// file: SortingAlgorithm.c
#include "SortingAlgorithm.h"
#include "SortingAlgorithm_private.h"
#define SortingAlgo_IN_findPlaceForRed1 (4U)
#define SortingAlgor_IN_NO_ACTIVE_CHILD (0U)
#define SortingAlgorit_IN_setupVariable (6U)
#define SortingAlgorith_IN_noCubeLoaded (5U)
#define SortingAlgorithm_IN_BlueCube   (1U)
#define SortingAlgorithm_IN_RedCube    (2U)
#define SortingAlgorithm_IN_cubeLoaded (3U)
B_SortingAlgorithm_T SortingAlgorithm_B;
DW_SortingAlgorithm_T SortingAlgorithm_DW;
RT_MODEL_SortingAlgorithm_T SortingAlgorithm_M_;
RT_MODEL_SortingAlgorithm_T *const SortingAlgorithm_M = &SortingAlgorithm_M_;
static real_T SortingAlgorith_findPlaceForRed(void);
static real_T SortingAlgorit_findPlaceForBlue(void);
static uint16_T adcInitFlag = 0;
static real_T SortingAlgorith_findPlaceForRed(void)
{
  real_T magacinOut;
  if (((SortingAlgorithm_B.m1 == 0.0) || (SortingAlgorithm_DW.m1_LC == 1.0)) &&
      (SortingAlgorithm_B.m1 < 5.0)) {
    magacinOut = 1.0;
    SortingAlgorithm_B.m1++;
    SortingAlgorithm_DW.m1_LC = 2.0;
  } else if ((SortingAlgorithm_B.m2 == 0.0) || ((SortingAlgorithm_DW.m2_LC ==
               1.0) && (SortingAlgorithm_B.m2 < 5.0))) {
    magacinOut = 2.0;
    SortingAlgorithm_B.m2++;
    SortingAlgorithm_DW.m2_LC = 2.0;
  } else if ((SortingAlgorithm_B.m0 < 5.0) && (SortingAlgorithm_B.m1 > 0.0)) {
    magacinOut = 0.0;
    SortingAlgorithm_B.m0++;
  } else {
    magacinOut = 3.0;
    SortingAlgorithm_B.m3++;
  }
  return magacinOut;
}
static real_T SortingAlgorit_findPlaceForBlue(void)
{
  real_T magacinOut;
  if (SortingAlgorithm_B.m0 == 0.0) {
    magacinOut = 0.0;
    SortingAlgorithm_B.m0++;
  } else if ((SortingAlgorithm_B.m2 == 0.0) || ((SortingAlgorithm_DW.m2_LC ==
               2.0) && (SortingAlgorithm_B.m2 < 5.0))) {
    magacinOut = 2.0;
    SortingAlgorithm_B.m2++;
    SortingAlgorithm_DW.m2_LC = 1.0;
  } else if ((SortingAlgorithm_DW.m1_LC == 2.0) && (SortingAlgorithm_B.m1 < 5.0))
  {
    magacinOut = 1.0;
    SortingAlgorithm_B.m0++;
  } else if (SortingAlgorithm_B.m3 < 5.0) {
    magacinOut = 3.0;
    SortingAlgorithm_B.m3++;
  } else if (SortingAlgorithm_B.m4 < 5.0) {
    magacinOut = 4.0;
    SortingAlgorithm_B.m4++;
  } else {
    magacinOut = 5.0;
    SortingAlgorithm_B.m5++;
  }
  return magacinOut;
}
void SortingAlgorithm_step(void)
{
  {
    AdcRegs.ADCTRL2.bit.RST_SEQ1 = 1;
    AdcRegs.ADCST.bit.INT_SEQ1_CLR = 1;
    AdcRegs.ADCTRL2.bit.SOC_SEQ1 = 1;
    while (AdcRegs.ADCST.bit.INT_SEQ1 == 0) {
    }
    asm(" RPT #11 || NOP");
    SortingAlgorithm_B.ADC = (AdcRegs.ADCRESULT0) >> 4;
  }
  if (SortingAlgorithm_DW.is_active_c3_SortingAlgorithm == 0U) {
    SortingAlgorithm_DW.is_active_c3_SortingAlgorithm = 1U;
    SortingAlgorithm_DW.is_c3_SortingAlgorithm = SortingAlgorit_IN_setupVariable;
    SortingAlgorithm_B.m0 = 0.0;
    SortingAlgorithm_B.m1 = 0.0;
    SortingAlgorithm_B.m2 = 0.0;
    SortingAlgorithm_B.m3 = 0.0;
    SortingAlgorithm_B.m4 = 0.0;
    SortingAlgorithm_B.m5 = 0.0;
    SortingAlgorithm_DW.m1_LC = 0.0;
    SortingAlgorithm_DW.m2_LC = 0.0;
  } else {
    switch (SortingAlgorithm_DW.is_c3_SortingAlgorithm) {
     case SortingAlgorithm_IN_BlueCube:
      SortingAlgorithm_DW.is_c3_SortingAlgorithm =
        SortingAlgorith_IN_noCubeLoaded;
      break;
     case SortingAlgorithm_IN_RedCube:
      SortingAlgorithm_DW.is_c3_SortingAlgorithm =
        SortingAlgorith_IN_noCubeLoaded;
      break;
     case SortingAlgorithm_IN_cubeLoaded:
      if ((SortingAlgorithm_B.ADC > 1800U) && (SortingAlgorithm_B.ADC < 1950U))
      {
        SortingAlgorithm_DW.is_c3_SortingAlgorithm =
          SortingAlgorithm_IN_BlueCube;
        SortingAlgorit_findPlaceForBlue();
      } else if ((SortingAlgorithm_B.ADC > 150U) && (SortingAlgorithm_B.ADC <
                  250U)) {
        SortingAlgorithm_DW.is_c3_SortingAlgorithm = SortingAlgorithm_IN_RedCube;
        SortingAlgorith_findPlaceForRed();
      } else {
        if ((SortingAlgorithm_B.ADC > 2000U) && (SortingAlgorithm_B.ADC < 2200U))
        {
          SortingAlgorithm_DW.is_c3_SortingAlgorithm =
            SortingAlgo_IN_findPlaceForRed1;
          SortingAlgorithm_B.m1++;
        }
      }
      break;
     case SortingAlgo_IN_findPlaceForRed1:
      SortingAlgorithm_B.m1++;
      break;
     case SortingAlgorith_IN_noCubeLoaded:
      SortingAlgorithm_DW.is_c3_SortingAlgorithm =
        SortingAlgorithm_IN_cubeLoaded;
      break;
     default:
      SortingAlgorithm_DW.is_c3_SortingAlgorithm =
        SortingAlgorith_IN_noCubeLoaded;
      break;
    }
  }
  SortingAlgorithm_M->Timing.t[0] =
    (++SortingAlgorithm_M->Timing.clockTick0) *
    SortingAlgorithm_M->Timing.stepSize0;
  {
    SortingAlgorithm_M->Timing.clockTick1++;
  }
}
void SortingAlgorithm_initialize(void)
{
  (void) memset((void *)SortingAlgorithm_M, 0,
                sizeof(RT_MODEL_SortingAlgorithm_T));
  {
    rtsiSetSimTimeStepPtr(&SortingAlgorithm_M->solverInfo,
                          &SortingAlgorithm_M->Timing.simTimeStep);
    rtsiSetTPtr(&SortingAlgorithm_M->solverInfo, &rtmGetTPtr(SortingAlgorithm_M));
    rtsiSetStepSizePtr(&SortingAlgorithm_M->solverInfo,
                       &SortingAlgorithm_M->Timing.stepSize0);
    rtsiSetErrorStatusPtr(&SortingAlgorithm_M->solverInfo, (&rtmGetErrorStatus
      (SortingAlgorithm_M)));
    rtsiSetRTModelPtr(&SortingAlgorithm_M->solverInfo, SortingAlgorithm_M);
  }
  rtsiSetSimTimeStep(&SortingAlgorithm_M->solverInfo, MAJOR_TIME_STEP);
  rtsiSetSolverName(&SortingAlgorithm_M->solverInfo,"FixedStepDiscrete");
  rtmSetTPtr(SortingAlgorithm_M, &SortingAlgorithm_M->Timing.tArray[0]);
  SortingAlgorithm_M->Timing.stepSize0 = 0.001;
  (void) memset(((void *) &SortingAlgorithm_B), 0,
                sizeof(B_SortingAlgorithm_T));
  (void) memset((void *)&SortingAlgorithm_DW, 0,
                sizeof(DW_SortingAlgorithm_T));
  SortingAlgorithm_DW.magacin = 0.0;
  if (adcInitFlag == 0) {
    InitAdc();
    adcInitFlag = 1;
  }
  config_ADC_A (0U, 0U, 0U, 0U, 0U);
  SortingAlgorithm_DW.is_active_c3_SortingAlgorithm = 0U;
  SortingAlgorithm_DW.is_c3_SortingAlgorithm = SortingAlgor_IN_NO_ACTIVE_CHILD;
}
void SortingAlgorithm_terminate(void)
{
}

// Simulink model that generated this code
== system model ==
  Stateflowchart#1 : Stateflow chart  <- 1: ADC
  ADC : c280xlib/ADC
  FromWorkspace#1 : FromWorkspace
== stateflow chart Stateflowchart#1 ==
  state setupVariable
    m0 = 0;
    m1 = 0;
    m2 = 0;
    m3 = 0;
    m4 = 0;
    m5 = 0;
    m6 = 0;
    magacin = 0;
    m0_LC = 0;
    m1_LC = 0;
    m2_LC = 0;
    m3_LC = 0;
    m4_LC = 0;
    m5_LC = 0;
    m6_LC = 0;
    magacin = -1;
  note: Motor fahre Position Mitte an
  state noCubeLoaded
  note: 1 ist Code for Blue, 2 is Code for Red, 3 is Code for Black, 0 is empty
  state cubeLoaded
  state findPlaceForRed1
    m1 = m1 + 1;
    magacin = 2;
  state RedCube
    magacin = findPlaceForRed();
  state BlueCube
    magacin = findPlaceForBlue()
  setupVariable -> noCubeLoaded
  (default) -> setupVariable
  BlueCube -> noCubeLoaded
  RedCube -> noCubeLoaded
  noCubeLoaded -> cubeLoaded
  cubeLoaded -> findPlaceForRed1 [order 3] : [(color > 2000 & color < 2200)]
  cubeLoaded -> RedCube [order 2] : [(color > 150 & color < 250)]
  cubeLoaded -> BlueCube [order 1] : [(color > 1800 & color < 1950) ]
  data: magacinOut function_output; magacinOut function_output; color input; cubeLoaded input; m6 local; m0_LC local; m3_LC local; m2_LC local; m5_LC local; m1_LC local; m6_LC local; m4_LC local; m1 output; m2 output; m5 output; m4 output; m3 output; m0 output; magacin output
  function magacinOut  = findPlaceForRed:
    | function magacinOut  = findPlaceForRed
    | 
    | %1 ist Code for Blue, 2 is Code for Red, 3 is Code for Black, 0 is empty
    | if((m1 == 0 || m1_LC == 1)&& m1 < 5) 
    |             magacinOut = 1;
    |             m1 = m1 + 1;
    |             m1_LC = 2;
    | elseif (m2 == 0 || (m2_LC == 1 && m2 < 5))
    |             magacinOut = 2;
    |             m2 = m2 + 1; 
    |             m2_LC = 2;
    | elseif (m0 < 5 && m1 > 0)
    |             magacinOut = 0;
    |             m0 = m0 + 1;
    |             m0_LC = 2;
    | else 
    |             magacinOut = 3;
    |             m3 = m3 + 1;
    |             m3_LC = 2;
    | end
  function magacinOut  = findPlaceForBlue:
    | function magacinOut  = findPlaceForBlue
    | 
    | %1 ist Code for Blue, 2 is Code for Red, 3 is Code for Black, 0 is empty
    | if(m0 == 0) 
    |             magacinOut = 0;
    |             m0 = m0 + 1;
    |             m0_LC = 1;
    | elseif (m2 == 0) || (m2_LC == 2 && m2 < 5)
    |             magacinOut = 2;
    |             m2 = m2 + 1; 
    |             m2_LC = 1;
    | elseif (m1_LC == 2 && m1 < 5)
    |             magacinOut = 1;
    |             m0 = m0 + 1;
    |             m0_LC = 1;
    | elseif m3 < 5
    |             magacinOut = 3;
    |             m3 = m3 + 1;
    | elseif m4 < 5
    |             magacinOut = 4;
    |             m4 = m4 + 1;
    | else
    |             magacinOut = 5;
    |             m5 = m5 + 1;
    | end
